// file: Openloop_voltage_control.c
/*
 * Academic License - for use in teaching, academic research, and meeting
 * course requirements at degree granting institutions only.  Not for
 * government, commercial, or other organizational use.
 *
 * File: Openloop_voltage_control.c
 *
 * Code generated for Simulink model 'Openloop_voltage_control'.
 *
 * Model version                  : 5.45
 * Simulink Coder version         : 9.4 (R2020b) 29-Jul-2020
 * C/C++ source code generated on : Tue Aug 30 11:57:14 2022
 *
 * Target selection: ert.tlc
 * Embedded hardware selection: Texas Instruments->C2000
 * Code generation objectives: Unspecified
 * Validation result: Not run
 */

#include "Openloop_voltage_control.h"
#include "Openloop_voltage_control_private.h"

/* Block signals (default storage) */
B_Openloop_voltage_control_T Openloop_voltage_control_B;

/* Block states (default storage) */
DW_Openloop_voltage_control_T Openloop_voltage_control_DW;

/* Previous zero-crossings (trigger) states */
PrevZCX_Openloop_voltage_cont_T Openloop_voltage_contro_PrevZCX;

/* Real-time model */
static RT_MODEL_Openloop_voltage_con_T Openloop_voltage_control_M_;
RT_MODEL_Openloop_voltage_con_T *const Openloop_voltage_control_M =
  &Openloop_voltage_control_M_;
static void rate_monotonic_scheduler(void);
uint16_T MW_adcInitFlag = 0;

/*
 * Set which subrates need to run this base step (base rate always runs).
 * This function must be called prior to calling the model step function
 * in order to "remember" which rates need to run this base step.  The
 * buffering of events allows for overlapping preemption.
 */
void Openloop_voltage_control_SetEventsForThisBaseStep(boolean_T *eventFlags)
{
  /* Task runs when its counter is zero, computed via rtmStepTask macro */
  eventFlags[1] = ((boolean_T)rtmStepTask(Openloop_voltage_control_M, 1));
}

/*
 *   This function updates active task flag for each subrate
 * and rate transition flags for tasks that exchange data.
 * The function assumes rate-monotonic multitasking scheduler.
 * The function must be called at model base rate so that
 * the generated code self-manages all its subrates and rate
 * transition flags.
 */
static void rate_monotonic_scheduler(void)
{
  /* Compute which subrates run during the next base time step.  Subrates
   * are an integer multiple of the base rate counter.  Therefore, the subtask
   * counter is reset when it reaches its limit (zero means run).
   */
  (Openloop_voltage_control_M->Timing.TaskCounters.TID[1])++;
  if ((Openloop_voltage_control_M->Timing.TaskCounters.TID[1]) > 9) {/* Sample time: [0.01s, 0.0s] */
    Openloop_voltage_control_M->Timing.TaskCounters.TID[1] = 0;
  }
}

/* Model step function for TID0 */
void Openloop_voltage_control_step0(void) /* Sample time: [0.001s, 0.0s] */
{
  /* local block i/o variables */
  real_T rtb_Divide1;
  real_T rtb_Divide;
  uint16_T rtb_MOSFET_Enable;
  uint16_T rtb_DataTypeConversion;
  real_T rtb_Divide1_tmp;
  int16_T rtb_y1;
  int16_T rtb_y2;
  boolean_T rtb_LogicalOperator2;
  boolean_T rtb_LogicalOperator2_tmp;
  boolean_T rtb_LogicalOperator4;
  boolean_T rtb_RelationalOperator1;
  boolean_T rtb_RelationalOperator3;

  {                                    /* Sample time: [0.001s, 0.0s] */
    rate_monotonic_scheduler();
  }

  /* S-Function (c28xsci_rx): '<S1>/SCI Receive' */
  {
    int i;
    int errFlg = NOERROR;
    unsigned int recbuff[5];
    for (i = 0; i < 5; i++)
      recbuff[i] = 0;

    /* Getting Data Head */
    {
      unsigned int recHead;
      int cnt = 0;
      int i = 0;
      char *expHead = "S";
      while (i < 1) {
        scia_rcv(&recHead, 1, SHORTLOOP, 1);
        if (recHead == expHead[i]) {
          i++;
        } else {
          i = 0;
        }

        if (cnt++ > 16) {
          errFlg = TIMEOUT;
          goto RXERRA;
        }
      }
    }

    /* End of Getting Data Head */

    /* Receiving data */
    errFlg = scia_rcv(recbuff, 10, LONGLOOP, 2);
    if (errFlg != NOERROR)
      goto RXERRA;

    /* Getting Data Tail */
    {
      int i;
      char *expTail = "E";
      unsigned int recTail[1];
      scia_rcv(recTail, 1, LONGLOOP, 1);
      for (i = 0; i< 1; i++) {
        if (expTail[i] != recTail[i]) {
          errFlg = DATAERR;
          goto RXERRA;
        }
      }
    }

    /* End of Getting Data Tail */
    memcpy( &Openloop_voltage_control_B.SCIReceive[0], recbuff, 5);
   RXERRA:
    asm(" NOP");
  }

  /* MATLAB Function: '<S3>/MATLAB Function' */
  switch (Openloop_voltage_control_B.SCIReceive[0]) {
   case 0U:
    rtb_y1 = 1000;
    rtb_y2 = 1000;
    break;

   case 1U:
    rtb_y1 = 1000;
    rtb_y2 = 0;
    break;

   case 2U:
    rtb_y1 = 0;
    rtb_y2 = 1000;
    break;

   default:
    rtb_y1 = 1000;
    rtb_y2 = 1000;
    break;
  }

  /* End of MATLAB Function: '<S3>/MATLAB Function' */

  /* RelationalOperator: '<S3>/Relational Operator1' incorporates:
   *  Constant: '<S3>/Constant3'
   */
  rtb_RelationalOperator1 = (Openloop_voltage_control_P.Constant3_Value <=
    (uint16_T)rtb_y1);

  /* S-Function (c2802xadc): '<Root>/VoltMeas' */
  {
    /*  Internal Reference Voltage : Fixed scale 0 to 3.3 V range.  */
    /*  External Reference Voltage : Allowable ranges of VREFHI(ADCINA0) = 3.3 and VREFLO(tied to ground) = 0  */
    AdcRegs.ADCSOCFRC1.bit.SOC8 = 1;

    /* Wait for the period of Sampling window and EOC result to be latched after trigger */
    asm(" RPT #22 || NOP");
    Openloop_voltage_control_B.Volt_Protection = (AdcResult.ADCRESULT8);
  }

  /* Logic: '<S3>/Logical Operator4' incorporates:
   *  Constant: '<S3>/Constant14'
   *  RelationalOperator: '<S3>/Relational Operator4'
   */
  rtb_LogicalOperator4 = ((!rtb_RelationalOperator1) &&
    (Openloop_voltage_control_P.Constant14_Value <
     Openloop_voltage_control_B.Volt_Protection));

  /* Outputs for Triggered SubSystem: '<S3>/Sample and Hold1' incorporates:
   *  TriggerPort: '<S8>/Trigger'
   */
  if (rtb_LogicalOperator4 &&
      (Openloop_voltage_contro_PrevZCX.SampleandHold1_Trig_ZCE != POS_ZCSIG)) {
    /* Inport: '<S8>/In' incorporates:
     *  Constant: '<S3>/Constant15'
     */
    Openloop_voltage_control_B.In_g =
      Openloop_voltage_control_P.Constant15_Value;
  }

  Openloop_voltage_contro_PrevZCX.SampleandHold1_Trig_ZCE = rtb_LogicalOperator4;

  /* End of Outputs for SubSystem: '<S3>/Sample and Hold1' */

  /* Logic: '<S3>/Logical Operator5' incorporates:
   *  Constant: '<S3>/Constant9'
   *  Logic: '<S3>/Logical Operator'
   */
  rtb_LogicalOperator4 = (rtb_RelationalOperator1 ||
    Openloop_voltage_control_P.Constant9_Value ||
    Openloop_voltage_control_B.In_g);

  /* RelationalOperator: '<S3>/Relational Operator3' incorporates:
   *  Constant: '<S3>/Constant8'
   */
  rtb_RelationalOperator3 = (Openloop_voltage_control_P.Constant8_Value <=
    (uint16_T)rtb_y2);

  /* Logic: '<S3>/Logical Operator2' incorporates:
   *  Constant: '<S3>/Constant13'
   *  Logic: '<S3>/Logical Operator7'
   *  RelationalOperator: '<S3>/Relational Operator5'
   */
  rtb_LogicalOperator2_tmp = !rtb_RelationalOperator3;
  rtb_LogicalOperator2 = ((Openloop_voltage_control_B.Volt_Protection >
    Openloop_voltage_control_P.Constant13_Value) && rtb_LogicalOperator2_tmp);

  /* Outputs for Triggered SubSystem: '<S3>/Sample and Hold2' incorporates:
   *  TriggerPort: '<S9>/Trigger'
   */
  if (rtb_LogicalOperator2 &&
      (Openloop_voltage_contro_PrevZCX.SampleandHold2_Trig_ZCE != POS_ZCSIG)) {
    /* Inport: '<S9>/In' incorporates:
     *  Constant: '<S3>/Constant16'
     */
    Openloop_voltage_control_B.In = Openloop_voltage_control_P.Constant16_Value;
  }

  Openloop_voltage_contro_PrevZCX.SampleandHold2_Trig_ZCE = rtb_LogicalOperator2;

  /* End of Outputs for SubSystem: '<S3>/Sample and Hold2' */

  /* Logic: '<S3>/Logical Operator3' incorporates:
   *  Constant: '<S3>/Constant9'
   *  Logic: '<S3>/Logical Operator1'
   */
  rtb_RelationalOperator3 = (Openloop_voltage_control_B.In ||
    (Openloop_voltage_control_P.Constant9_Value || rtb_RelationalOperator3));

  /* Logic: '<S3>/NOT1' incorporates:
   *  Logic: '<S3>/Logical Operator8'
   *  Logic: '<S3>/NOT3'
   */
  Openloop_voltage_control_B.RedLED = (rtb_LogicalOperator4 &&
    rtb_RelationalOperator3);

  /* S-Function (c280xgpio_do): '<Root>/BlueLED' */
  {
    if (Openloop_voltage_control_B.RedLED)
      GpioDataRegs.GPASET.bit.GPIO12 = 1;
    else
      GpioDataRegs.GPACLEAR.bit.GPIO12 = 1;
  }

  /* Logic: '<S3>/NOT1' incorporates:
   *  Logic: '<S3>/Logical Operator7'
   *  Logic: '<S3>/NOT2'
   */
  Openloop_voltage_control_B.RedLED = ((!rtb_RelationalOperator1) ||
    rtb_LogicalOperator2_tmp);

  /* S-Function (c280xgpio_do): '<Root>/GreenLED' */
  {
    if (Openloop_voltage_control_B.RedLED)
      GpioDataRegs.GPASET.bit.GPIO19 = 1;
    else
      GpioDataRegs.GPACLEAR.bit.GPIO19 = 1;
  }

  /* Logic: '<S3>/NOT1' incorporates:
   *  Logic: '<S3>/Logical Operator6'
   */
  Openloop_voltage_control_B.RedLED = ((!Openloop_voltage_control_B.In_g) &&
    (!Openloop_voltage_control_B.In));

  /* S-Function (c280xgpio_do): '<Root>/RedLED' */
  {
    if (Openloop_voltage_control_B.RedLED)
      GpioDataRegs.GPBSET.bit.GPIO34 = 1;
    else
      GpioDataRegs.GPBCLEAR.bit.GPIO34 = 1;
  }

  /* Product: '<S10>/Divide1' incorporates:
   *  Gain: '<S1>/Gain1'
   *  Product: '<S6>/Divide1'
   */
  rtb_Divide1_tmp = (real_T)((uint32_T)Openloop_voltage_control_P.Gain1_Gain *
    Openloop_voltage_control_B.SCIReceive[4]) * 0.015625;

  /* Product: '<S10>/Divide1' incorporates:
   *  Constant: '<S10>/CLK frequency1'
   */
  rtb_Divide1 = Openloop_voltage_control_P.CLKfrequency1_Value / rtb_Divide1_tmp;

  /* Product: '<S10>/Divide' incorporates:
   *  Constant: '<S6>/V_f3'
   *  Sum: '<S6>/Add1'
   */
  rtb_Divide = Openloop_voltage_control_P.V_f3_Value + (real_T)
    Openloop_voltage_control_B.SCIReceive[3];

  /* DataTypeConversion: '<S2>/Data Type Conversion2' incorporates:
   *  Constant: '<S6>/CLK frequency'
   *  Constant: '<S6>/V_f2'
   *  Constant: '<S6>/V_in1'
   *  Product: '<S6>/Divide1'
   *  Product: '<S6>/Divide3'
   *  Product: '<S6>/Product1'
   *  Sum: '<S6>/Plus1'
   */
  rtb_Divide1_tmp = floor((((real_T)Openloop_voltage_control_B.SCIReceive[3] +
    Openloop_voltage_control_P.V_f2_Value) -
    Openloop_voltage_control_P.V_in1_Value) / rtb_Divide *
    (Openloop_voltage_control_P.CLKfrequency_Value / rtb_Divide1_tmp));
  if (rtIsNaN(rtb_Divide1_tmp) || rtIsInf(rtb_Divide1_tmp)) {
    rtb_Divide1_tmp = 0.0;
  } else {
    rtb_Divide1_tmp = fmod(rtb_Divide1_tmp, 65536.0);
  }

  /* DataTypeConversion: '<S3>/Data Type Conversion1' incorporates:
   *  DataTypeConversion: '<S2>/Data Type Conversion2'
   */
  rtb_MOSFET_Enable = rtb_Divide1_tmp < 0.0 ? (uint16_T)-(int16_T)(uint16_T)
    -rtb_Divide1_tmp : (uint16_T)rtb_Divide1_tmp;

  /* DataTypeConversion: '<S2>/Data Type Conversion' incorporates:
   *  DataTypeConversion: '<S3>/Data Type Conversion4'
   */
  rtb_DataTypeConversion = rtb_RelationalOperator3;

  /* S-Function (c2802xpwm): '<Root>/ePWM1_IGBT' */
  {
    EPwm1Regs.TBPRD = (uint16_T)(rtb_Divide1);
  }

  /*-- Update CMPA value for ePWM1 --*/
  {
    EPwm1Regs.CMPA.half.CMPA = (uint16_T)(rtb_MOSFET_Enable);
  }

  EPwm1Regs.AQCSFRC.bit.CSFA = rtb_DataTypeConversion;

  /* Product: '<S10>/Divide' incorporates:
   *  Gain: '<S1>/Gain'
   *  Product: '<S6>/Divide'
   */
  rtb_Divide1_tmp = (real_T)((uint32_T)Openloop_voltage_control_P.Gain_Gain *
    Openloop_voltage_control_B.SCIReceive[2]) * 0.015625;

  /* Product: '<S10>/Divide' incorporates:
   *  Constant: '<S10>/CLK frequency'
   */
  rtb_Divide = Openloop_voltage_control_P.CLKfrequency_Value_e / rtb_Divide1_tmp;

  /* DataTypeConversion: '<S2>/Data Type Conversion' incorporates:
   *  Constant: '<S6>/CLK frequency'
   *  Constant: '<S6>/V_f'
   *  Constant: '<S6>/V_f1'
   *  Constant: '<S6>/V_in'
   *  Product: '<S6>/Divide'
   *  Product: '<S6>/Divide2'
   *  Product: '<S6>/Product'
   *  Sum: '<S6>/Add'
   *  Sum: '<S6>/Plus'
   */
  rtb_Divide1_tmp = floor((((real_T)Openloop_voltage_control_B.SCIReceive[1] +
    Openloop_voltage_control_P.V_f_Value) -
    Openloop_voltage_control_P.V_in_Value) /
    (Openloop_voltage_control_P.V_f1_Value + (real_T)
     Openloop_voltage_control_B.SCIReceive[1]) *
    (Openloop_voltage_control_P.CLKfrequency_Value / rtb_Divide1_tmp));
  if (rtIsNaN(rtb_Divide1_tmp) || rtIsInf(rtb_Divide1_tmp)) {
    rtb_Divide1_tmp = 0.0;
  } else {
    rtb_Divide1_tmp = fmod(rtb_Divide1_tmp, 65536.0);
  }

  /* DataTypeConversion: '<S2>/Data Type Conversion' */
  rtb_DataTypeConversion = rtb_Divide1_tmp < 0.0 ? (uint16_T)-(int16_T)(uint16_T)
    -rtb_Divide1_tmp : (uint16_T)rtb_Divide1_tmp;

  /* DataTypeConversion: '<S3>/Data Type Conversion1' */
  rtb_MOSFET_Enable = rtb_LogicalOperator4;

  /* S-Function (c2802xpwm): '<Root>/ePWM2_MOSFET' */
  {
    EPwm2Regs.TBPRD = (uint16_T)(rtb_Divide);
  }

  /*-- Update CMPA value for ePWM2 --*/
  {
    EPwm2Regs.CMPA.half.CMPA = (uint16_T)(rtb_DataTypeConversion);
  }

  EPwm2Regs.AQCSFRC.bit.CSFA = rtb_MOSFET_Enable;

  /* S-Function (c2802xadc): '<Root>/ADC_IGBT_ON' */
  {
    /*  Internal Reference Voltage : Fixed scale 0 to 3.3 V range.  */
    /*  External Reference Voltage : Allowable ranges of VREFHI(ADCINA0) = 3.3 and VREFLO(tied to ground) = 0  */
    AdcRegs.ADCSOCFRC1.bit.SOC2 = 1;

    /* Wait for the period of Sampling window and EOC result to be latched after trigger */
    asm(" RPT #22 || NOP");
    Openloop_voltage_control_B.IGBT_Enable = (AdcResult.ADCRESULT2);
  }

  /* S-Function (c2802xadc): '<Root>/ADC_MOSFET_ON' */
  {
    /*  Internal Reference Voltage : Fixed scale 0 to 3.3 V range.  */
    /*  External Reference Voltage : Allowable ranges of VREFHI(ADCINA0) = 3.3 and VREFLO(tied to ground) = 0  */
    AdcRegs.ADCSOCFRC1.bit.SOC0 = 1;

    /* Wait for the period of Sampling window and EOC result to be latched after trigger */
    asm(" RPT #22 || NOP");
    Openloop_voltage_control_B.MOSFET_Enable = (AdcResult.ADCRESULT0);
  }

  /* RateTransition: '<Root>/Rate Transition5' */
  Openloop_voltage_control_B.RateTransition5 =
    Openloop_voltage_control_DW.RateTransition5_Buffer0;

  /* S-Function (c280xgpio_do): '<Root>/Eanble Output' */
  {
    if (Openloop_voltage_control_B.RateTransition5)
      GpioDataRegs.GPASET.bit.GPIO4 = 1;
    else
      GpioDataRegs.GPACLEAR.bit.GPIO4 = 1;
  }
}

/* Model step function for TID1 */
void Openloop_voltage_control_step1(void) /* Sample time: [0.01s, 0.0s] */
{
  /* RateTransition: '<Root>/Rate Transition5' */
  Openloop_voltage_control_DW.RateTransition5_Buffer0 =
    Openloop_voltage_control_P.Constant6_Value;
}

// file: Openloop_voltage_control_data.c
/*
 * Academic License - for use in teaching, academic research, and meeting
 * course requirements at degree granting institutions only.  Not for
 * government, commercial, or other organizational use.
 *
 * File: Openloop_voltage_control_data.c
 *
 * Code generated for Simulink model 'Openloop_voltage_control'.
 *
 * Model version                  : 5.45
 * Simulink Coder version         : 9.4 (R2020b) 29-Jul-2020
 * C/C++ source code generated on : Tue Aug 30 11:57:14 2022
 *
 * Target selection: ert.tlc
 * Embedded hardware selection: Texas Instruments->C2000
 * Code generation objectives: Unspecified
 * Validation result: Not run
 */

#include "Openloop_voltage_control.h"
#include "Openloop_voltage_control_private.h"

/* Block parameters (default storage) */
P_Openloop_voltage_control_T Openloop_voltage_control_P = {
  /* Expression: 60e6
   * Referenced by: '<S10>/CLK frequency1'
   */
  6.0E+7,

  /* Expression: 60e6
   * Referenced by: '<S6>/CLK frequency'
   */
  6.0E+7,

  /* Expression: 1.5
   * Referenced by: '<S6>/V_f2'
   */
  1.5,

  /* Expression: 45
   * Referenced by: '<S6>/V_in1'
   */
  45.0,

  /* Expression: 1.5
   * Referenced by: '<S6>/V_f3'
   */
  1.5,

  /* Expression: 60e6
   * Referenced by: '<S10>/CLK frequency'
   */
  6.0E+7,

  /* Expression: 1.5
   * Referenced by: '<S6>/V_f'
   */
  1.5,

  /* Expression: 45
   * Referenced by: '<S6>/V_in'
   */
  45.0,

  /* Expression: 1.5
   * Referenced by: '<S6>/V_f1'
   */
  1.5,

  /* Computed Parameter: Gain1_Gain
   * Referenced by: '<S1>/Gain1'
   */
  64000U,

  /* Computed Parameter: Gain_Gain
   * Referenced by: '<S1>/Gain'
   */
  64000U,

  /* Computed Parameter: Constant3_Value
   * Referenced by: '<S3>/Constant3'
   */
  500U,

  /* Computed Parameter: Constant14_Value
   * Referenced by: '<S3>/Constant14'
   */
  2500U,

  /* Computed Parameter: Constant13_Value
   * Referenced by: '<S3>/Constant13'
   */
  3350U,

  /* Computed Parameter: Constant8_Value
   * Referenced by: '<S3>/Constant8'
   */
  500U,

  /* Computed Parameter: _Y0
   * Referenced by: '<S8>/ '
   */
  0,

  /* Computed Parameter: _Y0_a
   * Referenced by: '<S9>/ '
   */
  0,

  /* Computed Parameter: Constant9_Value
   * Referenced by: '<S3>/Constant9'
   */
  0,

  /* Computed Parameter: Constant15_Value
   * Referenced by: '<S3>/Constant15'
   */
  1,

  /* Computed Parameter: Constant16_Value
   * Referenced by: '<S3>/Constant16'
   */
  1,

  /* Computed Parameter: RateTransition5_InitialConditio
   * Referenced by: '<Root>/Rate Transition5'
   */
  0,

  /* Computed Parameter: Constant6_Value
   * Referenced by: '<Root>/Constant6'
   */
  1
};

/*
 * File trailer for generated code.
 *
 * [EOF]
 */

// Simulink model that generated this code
simulink model "Openloop_voltage_control"  (R2020b)
settings: Solver=FixedStepDiscrete  StartTime=0.0  StopTime=Inf  RelTol=1e-3  EnableMultiTasking=on
undefined symbols (not defined in the file): C2000, Clear, D_IGBT_CCM, D_MOSFET_CCM, Disable, ePWM2, ePWMxA, GPTRIP1SEL, GPTRIP2SEL, Immediate, Positive, Set, Timer_period_IGBT, Timer_period_MOSFET, TZ1, TZ2, Up
libraries: c2802xlib x9, dspsigops x2, c280xlib x1

== system Openloop_voltage_control ==
  note: Enable PWM
  ADC_IGBT_ON : c2802xlib/ADC  blkParamProc=C2000  ADCModule=1  samplingMode=Single sample mode  ADCResolution=12-bit (Single-ended input)  useSOC1=SOC2  useSOC2=SOC0_SOC1  SOCAcquisitionWindow=7  SOCTriggerSource=Software  SOCInterruptTrigger=No ADCINT  Ts=0.001  dType=uint16  postInterrupt=off  interruptSel=ADCINT1  ADCINTContinuous=off  endma=off  chdma=1  conv1=ADCINA3  conv2=ADCINA7 and ADCINB7  conv1_Type4=ADCIN0  conv2_Type4=ADCIN0 and ADCIN1
  ADC_MOSFET_ON : c2802xlib/ADC  blkParamProc=C2000  ADCModule=1  samplingMode=Single sample mode  ADCResolution=12-bit (Single-ended input)  useSOC1=SOC0  useSOC2=SOC0_SOC1  SOCAcquisitionWindow=7  SOCTriggerSource=Software  SOCInterruptTrigger=No ADCINT  Ts=0.001  dType=uint16  postInterrupt=off  interruptSel=ADCINT1  ADCINTContinuous=off  endma=off  chdma=1  conv1=ADCINA7  conv2=ADCINA7 and ADCINB7  conv1_Type4=ADCIN0  conv2_Type4=ADCIN0 and ADCIN1
  BlueLED : c2802xlib/Digital Output  GPIO_Number=GPIO8~GPIO15  GPIO_Bit0=off  GPIO_BIT0_Toggle=off  GPIO_Bit1=off  GPIO_BIT1_Toggle=off  GPIO_Bit2=off  GPIO_BIT2_Toggle=off  GPIO_Bit3=off  GPIO_BIT3_Toggle=off  GPIO_Bit4=on  GPIO_BIT4_Toggle=off  GPIO_Bit5=off  GPIO_BIT5_Toggle=off  GPIO_Bit6=off  GPIO_BIT6_Toggle=off  GPIO_Bit7=off  GPIO_BIT7_Toggle=off
  Constant6 : Constant  OutDataTypeStr=boolean  SampleTime=0.01
  Dashboard receiver block : Subsystem
  Demux : Demux  Outputs=3
  Duty Cycles : Subsystem
  Eanble Output : c2802xlib/Digital Output  GPIO_Number=GPIO0~GPIO7  GPIO_Bit0=off  GPIO_BIT0_Toggle=off  GPIO_Bit1=off  GPIO_BIT1_Toggle=off  GPIO_Bit2=off  GPIO_BIT2_Toggle=off  GPIO_Bit3=off  GPIO_BIT3_Toggle=off  GPIO_Bit4=on  GPIO_BIT4_Toggle=off  GPIO_Bit5=off  GPIO_BIT5_Toggle=off  GPIO_Bit6=off  GPIO_BIT6_Toggle=off  GPIO_Bit7=off  GPIO_BIT7_Toggle=off
  GreenLED : c2802xlib/Digital Output  GPIO_Number=GPIO16~GPIO23  GPIO_Bit0=off  GPIO_BIT0_Toggle=off  GPIO_Bit1=off  GPIO_BIT1_Toggle=off  GPIO_Bit2=off  GPIO_BIT2_Toggle=off  GPIO_Bit3=on  GPIO_BIT3_Toggle=off  GPIO_Bit4=off  GPIO_BIT4_Toggle=off  GPIO_Bit5=off  GPIO_BIT5_Toggle=off  GPIO_Bit6=off  GPIO_BIT6_Toggle=off  GPIO_Bit7=off  GPIO_BIT7_Toggle=off
  Logic circuit : Subsystem
  Rate Transition10 : RateTransition  Deterministic=off
  Rate Transition3 : RateTransition
  Rate Transition5 : RateTransition  Deterministic=off
  Rate Transition7 : RateTransition
  Rate Transition8 : RateTransition  Deterministic=off  InitialCondition=1
  Rate Transition9 : RateTransition  Deterministic=off
  RedLED : c2802xlib/Digital Output  GPIO_Number=GPIO32~GPIO34  GPIO_Bit0=off  GPIO_BIT0_Toggle=off  GPIO_Bit1=off  GPIO_BIT1_Toggle=off  GPIO_Bit2=on  GPIO_BIT2_Toggle=off  GPIO_Bit3=off  GPIO_BIT3_Toggle=off  GPIO_Bit4=off  GPIO_BIT4_Toggle=off  GPIO_Bit5=off  GPIO_BIT5_Toggle=off  GPIO_Bit6=off  GPIO_BIT6_Toggle=off  GPIO_Bit7=off  GPIO_BIT7_Toggle=off
  Timer : Subsystem
  VoltMeas : c2802xlib/ADC  blkParamProc=C2000  ADCModule=1  samplingMode=Single sample mode  ADCResolution=12-bit (Single-ended input)  useSOC1=SOC8  useSOC2=SOC0_SOC1  SOCAcquisitionWindow=7  SOCTriggerSource=Software  SOCInterruptTrigger=No ADCINT  Ts=0.001  dType=uint16  postInterrupt=off  interruptSel=ADCINT1  ADCINTContinuous=off  endma=off  chdma=1  conv1=ADCINB1  conv2=ADCINA7 and ADCINB7  conv1_Type4=ADCIN0  conv2_Type4=ADCIN0 and ADCIN1
  ePWM1_IGBT : c2802xlib/ePWM  PwmType=C2000  useModule=ePWM1  ePWMxLINKTBPRD=Not Linked  periodUnits=Clock cycles  timerSource=Input port  timerPeriod_clk=Timer_period_IGBT*2  timerPeriod_sec=0.0001  tbshadow=Counter equals to zero  countingMode=Up  phaseActiveEnable=Disable  phaseDirection=Count down after sync  phaseActive=0  synchronizationEnable=off  dcaevt1Sync=off  dcbevt1Sync=off  synchronizationOption=Disable  perSynchronizationOption=Counter equals to period (CTR=PRD)  clockPrescale=1  HSclockPrescale=1  enswap=off  ePWMxAStatus=on  ePWMxAactionLogic1=Set  ePWMxAactionLogic2=Set  ePWMxAactionLogic3=Clear  ePWMxAactionLogic4=Set  ePWMxAactionLogic5=Do nothing  ePWMxAactionLogic6=Do nothing  ePWMxACSFenable=on  ePWMxACSFvalue=Forcing disable  ePWMxASFreload=Immediate  ePWMxBStatus=off  ePWMxBactionLogic1=Set  ePWMxBactionLogic2=Clear  ePWMxBactionLogic3=Do nothing  ePWMxBactionLogic4=Do nothing  ePWMxBactionLogic5=Clear  ePWMxBactionLogic6=Set  ePWMxBCSFenable=off  ePWMxBCSFvalue=Forcing disable  ePWMxBSFreload=Immediate  ePWNxBOutWay=off  ePWMxLINKCMPA=Not Linked  CMPAUnits=Clock cycles  CMPASource=Input port  CMPAValue_per=50  CMPAValue_clk=2000  enCMPAshadow=Counter equals to zero (CTR=Zero)  ePWMxLINKCMPB=Not Linked  CMPBUnits=Clock cycles  CMPBSource=Specify via dialog  CMPBValue_per=50  CMPBValue_clk=32000  enCMPBshadow=Counter equals to zero (CTR=Zero)  ePWMxLINKCMPC=Not Linked  CMPCUnits=Clock cycles  CMPCSource=Specify via dialog  CMPCValue_per=50  CMPCValue_clk=32000  enCMPCshadow=Counter equals to zero (CTR=Zero)  ePWMxLINKCMPD=Not Linked  CMPDUnits=Clock cycles  CMPDSource=Specify via dialog  CMPDValue_per=50  CMPDValue_clk=32000  enCMPDshadow=Counter equals to zero (CTR=Zero)  enableDBePWMxA=off  enableDBePWMxB=off  enhalfcycle=off  DBpolarity=Active high (AH)  DBedgeDelay=Positive  DBSource_ePWMxA=ePWMxA  DBSource_ePWMxB=ePWMxA  DBPeriodUnits=Clock cycles  DBperiodSource=Specify via dialog  REDperiod=0  FEDperiod=0  REDperiod_sec=0  FEDperiod_sec=0  LoadModeDBRED=Immediate without using shadow  LoadModeDBFED=Immediate without using shadow  adcstartModuleA=off  adcrequestEventA=First event  adcstartEventA=Digital Compare Module A Event 1 start of conversion (DCAEVT1.soc)  adcstartEventA_type2=Digital Compare Module A Event 1 start of conversion (DCAEVT1.soc)  adcstartModuleB=off  adcrequestEventB=First event  adcstartEventB=Counter equals to zero (CTR=Zero)  adcstartEventB_type2=Counter equals to zero (CTR=Zero)  intEn=off  intPrd=First event  intSel=Counter equals to zero (CTR=Zero)  intSel_type2=Counter equals to zero (CTR=Zero)  hrpe=off  enHRPWM=off  HRPWM_LoadMode=Counter equals to period (CTR=PRD)  HRPWM_CTLMode=Duty or Period control mode  HRPWM_EDGMode=Both edge  hrpeb=off  enHRPWMB=off  HRPWM_LoadModeB=Counter equals to zero (CTR=ZERO)  HRPWM_CTLModeB=Duty or Period control mode  HRPWM_EDGModeB=Both edge  enHRDBRED=off  enHRDBFED=off  enSFO=on  enautoconv=on  chopperEnable=off  chopperFrequency=1  chopperFirstwidth=1  chopperDuty=12.5%  tripZonesource=Specify via dialog  tzselOSHT1=off  tzselOSHT2=off  tzselOSHT3=off  tzselOSHDCAEV1=off  tzselOSHDCBEV1=off  tzselCBC1=off  tzselCBC2=off  tzselCBC3=off  tzselCBCDCAEV2=off  tzselCBCDCBEV2=off  tzselOSHT4=off  tzselOSHT5=off  tzselOSHT6=off  tzselCBC4=off  tzselCBC5=off  tzselCBC6=off  enTzOstIntr=off  enTzCbcIntr=off  enTzDCAEVT1Intr=off  enTzDCAEVT2Intr=off  enTzDCBEVT1Intr=off  enTzDCBEVT2Intr=off  ePWMxAforced=No action  ePWMxBforced=No action  DCAEVT1forced=No action  DCBEVT1forced=No action  DCAEVT2forced=No action  DCBEVT2forced=No action  dcah=Trip Zone 1 input (TZ1)  dcal=Trip Zone 2 input (TZ2)  dcbh=Trip Zone 1 input (TZ1)  dcbl=Trip Zone 2 input (TZ2)  dcah_type2=GPTRIP1SEL/(TZ1)  dcal_type2=GPTRIP2SEL/(TZ2)  dcbh_type2=GPTRIP1SEL/(TZ1)  dcbl_type2=GPTRIP2SEL/(TZ2)  gendcaevt1=Event disabled  gendcaevt2=Event disabled  gendcbevt1=Event disabled  gendcbevt2=Event disabled  dcaevt1src=DCAEVT1 with sync  dcaevt2src=DCAEVT2 with sync  dcbevt1src=DCBEVT1 with sync  dcbevt2src=DCBEVT2 with sync  pulsesel=Counter equals to zero (CTR=Zero)  blankinv=off  blankoffset=0  blankwidth=0  evsrcsel=Filtered version of DCAEVT1 (DCAEVT1FILT)  encape=off
  ePWM2_MOSFET : c2802xlib/ePWM  PwmType=C2000  useModule=ePWM2  ePWMxLINKTBPRD=Not Linked  periodUnits=Clock cycles  timerSource=Input port  timerPeriod_clk=timerPeriod_clk  timerPeriod_sec=timerPeriod_sec  tbshadow=Counter equals to zero  countingMode=Up  phaseActiveEnable=Disable  phaseDirection=Count down after sync  phaseActive=phaseActive  synchronizationEnable=off  dcaevt1Sync=off  dcbevt1Sync=off  synchronizationOption=Disable  perSynchronizationOption=Counter equals to period (CTR=PRD)  clockPrescale=1  HSclockPrescale=1  enswap=off  ePWMxAStatus=on  ePWMxAactionLogic1=Set  ePWMxAactionLogic2=Set  ePWMxAactionLogic3=Clear  ePWMxAactionLogic4=Set  ePWMxAactionLogic5=Do nothing  ePWMxAactionLogic6=Do nothing  ePWMxACSFenable=on  ePWMxACSFvalue=Forcing disable  ePWMxASFreload=Immediate  ePWMxBStatus=off  ePWMxBactionLogic1=Set  ePWMxBactionLogic2=Clear  ePWMxBactionLogic3=Do nothing  ePWMxBactionLogic4=Do nothing  ePWMxBactionLogic5=Clear  ePWMxBactionLogic6=Set  ePWMxBCSFenable=off  ePWMxBCSFvalue=Forcing disable  ePWMxBSFreload=Immediate  ePWNxBOutWay=off  ePWMxLINKCMPA=Not Linked  CMPAUnits=Clock cycles  CMPASource=Input port  CMPAValue_per=CMPAValue_per  CMPAValue_clk=CMPAValue_clk  enCMPAshadow=Counter equals to zero (CTR=Zero)  ePWMxLINKCMPB=Not Linked  CMPBUnits=Clock cycles  CMPBSource=Specify via dialog  CMPBValue_per=CMPBValue_per  CMPBValue_clk=CMPBValue_clk  enCMPBshadow=Counter equals to zero (CTR=Zero)  ePWMxLINKCMPC=Not Linked  CMPCUnits=Clock cycles  CMPCSource=Specify via dialog  CMPCValue_per=CMPCValue_per  CMPCValue_clk=CMPCValue_clk  enCMPCshadow=Counter equals to zero (CTR=Zero)  ePWMxLINKCMPD=Not Linked  CMPDUnits=Clock cycles  CMPDSource=Specify via dialog  CMPDValue_per=CMPDValue_per  CMPDValue_clk=CMPDValue_clk  enCMPDshadow=Counter equals to zero (CTR=Zero)  enableDBePWMxA=off  enableDBePWMxB=off  enhalfcycle=off  DBpolarity=Active high (AH)  DBedgeDelay=Positive  DBSource_ePWMxA=ePWMxA  DBSource_ePWMxB=ePWMxA  DBPeriodUnits=Clock cycles  DBperiodSource=Specify via dialog  REDperiod=REDperiod  FEDperiod=FEDperiod  REDperiod_sec=REDperiod_sec  FEDperiod_sec=FEDperiod_sec  LoadModeDBRED=Immediate without using shadow  LoadModeDBFED=Immediate without using shadow  adcstartModuleA=off  adcrequestEventA=First event  adcstartEventA=Digital Compare Module A Event 1 start of conversion (DCAEVT1.soc)  adcstartEventA_type2=Digital Compare Module A Event 1 start of conversion (DCAEVT1.soc)  adcstartModuleB=off  adcrequestEventB=First event  adcstartEventB=Counter equals to zero (CTR=Zero)  adcstartEventB_type2=Counter equals to zero (CTR=Zero)  intEn=off  intPrd=First event  intSel=Counter equals to zero (CTR=Zero)  intSel_type2=Counter equals to zero (CTR=Zero)  hrpe=off  enHRPWM=off  HRPWM_LoadMode=Counter equals to period (CTR=PRD)  HRPWM_CTLMode=Duty or Period control mode  HRPWM_EDGMode=Both edge  hrpeb=off  enHRPWMB=off  HRPWM_LoadModeB=Counter equals to zero (CTR=ZERO)  HRPWM_CTLModeB=Duty or Period control mode  HRPWM_EDGModeB=Both edge  enHRDBRED=off  enHRDBFED=off  enSFO=on  enautoconv=on  chopperEnable=off  chopperFrequency=1  chopperFirstwidth=1  chopperDuty=12.5%  tripZonesource=Specify via dialog  tzselOSHT1=off  tzselOSHT2=off  tzselOSHT3=off  tzselOSHDCAEV1=off  tzselOSHDCBEV1=off  tzselCBC1=off  tzselCBC2=off  tzselCBC3=off  tzselCBCDCAEV2=off  tzselCBCDCBEV2=off  tzselOSHT4=off  tzselOSHT5=off  tzselOSHT6=off  tzselCBC4=off  tzselCBC5=off  tzselCBC6=off  enTzOstIntr=off  enTzCbcIntr=off  enTzDCAEVT1Intr=off  enTzDCAEVT2Intr=off  enTzDCBEVT1Intr=off  enTzDCBEVT2Intr=off  ePWMxAforced=No action  ePWMxBforced=No action  DCAEVT1forced=No action  DCBEVT1forced=No action  DCAEVT2forced=No action  DCBEVT2forced=No action  dcah=Trip Zone 1 input (TZ1)  dcal=Trip Zone 2 input (TZ2)  dcbh=Trip Zone 1 input (TZ1)  dcbl=Trip Zone 2 input (TZ2)  dcah_type2=GPTRIP1SEL/(TZ1)  dcal_type2=GPTRIP2SEL/(TZ2)  dcbh_type2=GPTRIP1SEL/(TZ1)  dcbl_type2=GPTRIP2SEL/(TZ2)  gendcaevt1=Event disabled  gendcaevt2=Event disabled  gendcbevt1=Event disabled  gendcbevt2=Event disabled  dcaevt1src=DCAEVT1 with sync  dcaevt2src=DCAEVT2 with sync  dcbevt1src=DCBEVT1 with sync  dcbevt2src=DCBEVT2 with sync  pulsesel=Counter equals to zero (CTR=Zero)  blankinv=off  blankoffset=blankoffset  blankwidth=blankwidth  evsrcsel=Filtered version of DCAEVT1 (DCAEVT1FILT)  encape=off  mask(C2802x/03x/05x/06x/M3x/37x/07x/004x/38x ePWM){PwmType=C2000, useModule=ePWM2, ePWMxLINKTBPRD=Not Linked, periodUnits=Clock cycles, timerSource=Input port, timerPeriod_clk=Timer_period_MOSFET*2, timerPeriod_sec=0.0001, tbshadow=Counter equals to zero, countingMode=Up, phaseActiveEnable=Disable, phaseDirection=Count down after sync, phaseActive=0, synchronizationEnable=off, dcaevt1Sync=off, dcbevt1Sync=off, synchronizationOption=Disable, perSynchronizationOption=Counter equals to period (CTR=PRD), clockPrescale=1, HSclockPrescale=1, enswap=off, ePWMxAStatus=on, ePWMxAactionLogic1=Set, ePWMxAactionLogic2=Set, ePWMxAactionLogic3=Clear, ePWMxAactionLogic4=Set, ePWMxAactionLogic5=Do nothing, ePWMxAactionLogic6=Do nothing, ePWMxACSFenable=on, ePWMxACSFvalue=Forcing disable, ePWMxASFreload=Immediate, ePWMxBStatus=off, ePWMxBactionLogic1=Set, ePWMxBactionLogic2=Clear, ePWMxBactionLogic3=Do nothing, ePWMxBactionLogic4=Do nothing, ePWMxBactionLogic5=Clear, ePWMxBactionLogic6=Set, ePWMxBCSFenable=off, ePWMxBCSFvalue=Forcing disable, ePWMxBSFreload=Immediate, ePWNxBOutWay=off, ePWMxLINKCMPA=Not Linked, CMPAUnits=Clock cycles, CMPASource=Input port, CMPAValue_per=50, CMPAValue_clk=525, enCMPAshadow=Counter equals to zero (CTR=Zero), ePWMxLINKCMPB=Not Linked, CMPBUnits=Clock cycles, CMPBSource=Specify via dialog, CMPBValue_per=50, CMPBValue_clk=32000, enCMPBshadow=Counter equals to zero (CTR=Zero), ePWMxLINKCMPC=Not Linked, CMPCUnits=Clock cycles, CMPCSource=Specify via dialog, CMPCValue_per=50, CMPCValue_clk=32000, enCMPCshadow=Counter equals to zero (CTR=Zero), ePWMxLINKCMPD=Not Linked, CMPDUnits=Clock cycles, CMPDSource=Specify via dialog, CMPDValue_per=50, CMPDValue_clk=32000, enCMPDshadow=Counter equals to zero (CTR=Zero), enableDBePWMxA=off, enableDBePWMxB=off, enhalfcycle=off, DBpolarity=Active high (AH), DBedgeDelay=Positive, DBSource_ePWMxA=ePWMxA, DBSource_ePWMxB=ePWMxA, DBPeriodUnits=Clock cycles, DBperiodSource=Specify via dialog, REDperiod=0, FEDperiod=0, REDperiod_sec=0, FEDperiod_sec=0, LoadModeDBRED=Immediate without using shadow, LoadModeDBFED=Immediate without using shadow, adcstartModuleA=off, adcrequestEventA=First event, adcstartEventA=Digital Compare Module A Event 1 start of conversion (DCAEVT1.soc), adcstartEventA_type2=Digital Compare Module A Event 1 start of conversion (DCAEVT1.soc), adcstartModuleB=off, adcrequestEventB=First event, adcstartEventB=Counter equals to zero (CTR=Zero), adcstartEventB_type2=Counter equals to zero (CTR=Zero), intEn=off, intPrd=First event, intSel=Counter equals to zero (CTR=Zero), intSel_type2=Counter equals to zero (CTR=Zero), hrpe=off, enHRPWM=off, HRPWM_LoadMode=Counter equals to period (CTR=PRD), HRPWM_CTLMode=Duty or Period control mode, HRPWM_EDGMode=Both edge, hrpeb=off, enHRPWMB=off, HRPWM_LoadModeB=Counter equals to zero (CTR=ZERO), HRPWM_CTLModeB=Duty or Period control mode, HRPWM_EDGModeB=Both edge, enHRDBRED=off, enHRDBFED=off, enSFO=on, enautoconv=on, chopperEnable=off, chopperFrequency=1, chopperFirstwidth=1, chopperDuty=12.5%, tripZonesource=Specify via dialog, tzselOSHT1=off, tzselOSHT2=off, tzselOSHT3=off, tzselOSHDCAEV1=off, tzselOSHDCBEV1=off, tzselCBC1=off, tzselCBC2=off, tzselCBC3=off, tzselCBCDCAEV2=off, tzselCBCDCBEV2=off, tzselOSHT4=off, tzselOSHT5=off, tzselOSHT6=off, tzselCBC4=off, tzselCBC5=off, tzselCBC6=off, enTzOstIntr=off, enTzCbcIntr=off, enTzDCAEVT1Intr=off, enTzDCAEVT2Intr=off, enTzDCBEVT1Intr=off, enTzDCBEVT2Intr=off, ePWMxAforced=No action, ePWMxBforced=No action, DCAEVT1forced=No action, DCBEVT1forced=No action, DCAEVT2forced=No action, DCBEVT2forced=No action, dcah=Trip Zone 1 input (TZ1), dcal=Trip Zone 2 input (TZ2), dcbh=Trip Zone 1 input (TZ1), dcbl=Trip Zone 2 input (TZ2), dcah_type2=GPTRIP1SEL/(TZ1), dcal_type2=GPTRIP2SEL/(TZ2), dcbh_type2=GPTRIP1SEL/(TZ1), dcbl_type2=GPTRIP2SEL/(TZ2), gendcaevt1=Event disabled, gendcaevt2=Event disabled, gendcbevt1=Event disabled, gendcbevt2=Event disabled, dcaevt1src=DCAEVT1 with sync, dcaevt2src=DCAEVT2 with sync, dcbevt1src=DCBEVT1 with sync, dcbevt2src=DCBEVT2 with sync, pulsesel=Counter equals to zero (CTR=Zero), blankinv=off, blankoffset=0, blankwidth=0, evsrcsel=Filtered version of DCAEVT1 (DCAEVT1FILT), encape=off}
      mask prompts: PwmType "BlockParameterProcessor"; useModule "Module:"; ePWMxLINKTBPRD "ePWMLink TBPRD"; periodUnits "Timer period units:"; timerSource "Specify timer period via:"; timerPeriod_clk "Timer period:"; timerPeriod_sec "Timer period:"; tbshadow "Reload for time base period register (PRDLD):"; countingMode "Counting mode:"; phaseActiveEnable "Synchronization action:"; phaseDirection "Counting direction after phase synchronization:"; phaseActive "Phase offset value (TBPHS):"; synchronizationEnable "Specify software synchronization via input port (SWFSYNC)"; dcaevt1Sync "Enable digital compare A event1 synchronization (DCAEVT1)"; dcbevt1Sync "Enable digital compare B event1 synchronization (DCBEVT1)"; synchronizationOption "Synchronization output (SYNCO):"; perSynchronizationOption "Peripheral synchronization event (PWMSYNCSEL):"; clockPrescale "Time base clock (TBCLK) prescaler divider:"; HSclockPrescale "High speed time base clock (HSPCLKDIV) prescaler divider:"; enswap "Enable swap module A and B"; ePWMxAStatus "Enable ePWM2A"; ePWMxAactionLogic1 "Action when counter=ZERO:"; ePWMxAactionLogic2 "Action when counter=period (PRD):"; ePWMxAactionLogic3 "Action when counter=CMPA on up-count (CAU):"; ePWMxAactionLogic4 "Action when counter=CMPA on down-count (CAD):"; ePWMxAactionLogic5 "Action when counter=CMPB on up-count (CBU):"; ePWMxAactionLogic6 "Action when counter=CMPB on down-count (CBD):"; ePWMxACSFenable "Add continuous software force input port"; ePWMxACSFvalue "Continuous software force logic:"; ePWMxASFreload "Reload condition for software force:"; ePWMxBStatus "Enable ePWM2B"; ePWMxBactionLogic1 "Action when counter=ZERO:"; ePWMxBactionLogic2 "Action when counter=period (PRD):"; ePWMxBactionLogic3 "Action when counter=CMPA on up-count (CAU):"; ePWMxBactionLogic4 "Action when counter=CMPA on down-count (CAD):"; ePWMxBactionLogic5 "Action when counter=CMPB on up-count (CBU):"; ePWMxBactionLogic6 "Action when counter=CMPB on down-count (CBD):"; ePWMxBCSFenable "Add continuous software force input port"; ePWMxBCSFvalue "Continuous software force logic:"; ePWMxBSFreload "Reload condition for software force:"; ePWNxBOutWay "Inverted version of ePWMxA"; ePWMxLINKCMPA "ePWMLink CMPA"; CMPAUnits "CMPA units:"; CMPASource "Specify CMPA via:"; CMPAValue_per "CMPA initial value:"; CMPAValue_clk "CMPA initial value:"; enCMPAshadow "Reload for compare A Register (SHDWAMODE):"; ePWMxLINKCMPB "ePWMLink CMPB"; CMPBUnits "CMPB units:"; CMPBSource "Specify CMPB via:"; CMPBValue_per "CMPB value:"; CMPBValue_clk "CMPB value:"; enCMPBshadow "Reload for compare B Register (SHDWBMODE):"; ePWMxLINKCMPC "ePWMLink CMPC"; CMPCUnits "CMPC units:"; CMPCSource "Specify CMPC via:"; CMPCValue_per "CMPC value:"; CMPCValue_clk "CMPC value:"; enCMPCshadow "Reload for compare C Register (SHDWCMODE):"; ePWMxLINKCMPD "ePWMLink CMPD"; CMPDUnits "CMPD units:"; CMPDSource "Specify CMPD via:"; CMPDValue_per "CMPD value:"; CMPDValue_clk "CMPD value:"; enCMPDshadow "Reload for compare D Register (SHDWDMODE):"; enableDBePWMxA "Use deadband for ePWM2A"; enableDBePWMxB "Use deadband for ePWM2B"; enhalfcycle "Enable half-cycle clocking"; DBpolarity "Deadband polarity:"; DBedgeDelay "Deadband polarity:"; DBSource_ePWMxA "Signal source for raising edge (RED):"; DBSource_ePWMxB "Signal source for falling edge (FED):"; DBPeriodUnits "Deadband period units:"; DBperiodSource "Deadband period source:"; REDperiod "Deadband Rising edge (RED) period (0~1023):"; FEDperiod "Deadband Falling edge (FED) period (0~1023):"; REDperiod_sec "Deadband Rising edge (RED) period:"; FEDperiod_sec "Deadband Falling edge (FED) period:"; LoadModeDBRED "Reload for DBRED register (SHDWDBRED):"; LoadModeDBFED "Reload for DBFED register (SHDWDBFED):"; adcstartModuleA "Enable ADC start of conversion for module A"; adcrequestEventA "Number of event for start of conversion A (SOCA) to be generated:"; adcstartEventA "Start of conversion for module A event selection:"; adcstartEventA_type2 "Start of conversion for module A event selection:"; adcstartModuleB "Enable ADC start of conversion for module B"; adcrequestEventB "Number of event for start of conversion B (SOCB) to be generated:"; adcstartEventB "Start of conversion for module B event selection:"; adcstartEventB_type2 "Start of conversion for module B event selection:"; intEn "Enable ePWM interrupt"; intPrd "Number of event for interrupt to be generated:"; intSel "Interrupt counter match event condition:"; intSel_type2 "Interrupt counter match event condition:"; hrpe "Enable High Resolution Period on ePWMxA(HRPWM-period)"; enHRPWM "Enable HRPWM Duty on ePWMxA(HRPWM-duty)"; HRPWM_LoadMode "High resolution PWM (HRPWM) Load mode on ePWMxA:"; HRPWM_CTLMode "High resolution PWM (HRPWM) control mode on ePWMxA:"; HRPWM_EDGMode "High resolution PWM (HRPWM) edge control mode on ePWMxA:"; hrpeb "Enable High Resolution Period on ePWMxB (HRPWM-period)"; enHRPWMB "Enable HRPWM Duty on ePWMxB (HRPWM-duty)"; HRPWM_LoadModeB "High resolution PWM (HRPWM) Load mode on ePWMxB:"; HRPWM_CTLModeB "High resolution PWM (HRPWM) control mode on ePWMxB:"; HRPWM_EDGModeB "High resolution PWM (HRPWM) edge control mode on ePWMxB:"; enHRDBRED "Enable high resolution deadband rising edge (RED)"; enHRDBFED "Enable high resolution deadband falling edge (FED)"; enSFO "Use scale factor optimizer (SFO) software"; enautoconv "Enable auto convert"; chopperEnable "Chopper module enable"; chopperFrequency "Chopper frequency divider:"; chopperFirstwidth "Chopper clock cycles width of first pulse:"; chopperDuty "Chopper pulse duty cycle:"; tripZonesource "Trip zone source:"; tzselOSHT1 "Enable one-shot trip-zone1 (TZ1)"; tzselOSHT2 "Enable one-shot trip-zone2 (TZ2)"; tzselOSHT3 "Enable one-shot trip-zone3 (TZ3)"; tzselOSHDCAEV1 "Enable one-shot digital compare A event 1 (DCAEVT1)"; tzselOSHDCBEV1 "Enable one-shot digital compare B event 1 (DCBEVT1)"; tzselCBC1 "Enable cyclic trip-zone1 (TZ1)"; tzselCBC2 "Enable cyclic trip-zone2 (TZ2)"; tzselCBC3 "Enable cyclic trip-zone3 (TZ3)"; tzselCBCDCAEV2 "Enable cyclic digital compare A event 2 (DCAEVT2)"; tzselCBCDCBEV2 "Enable cyclic digital compare B event 2 (DCBEVT2)"; tzselOSHT4 "Enable one-shot trip-zone4 (TZ4)"; tzselOSHT5 "Enable one-shot trip-zone5 (TZ5)"; tzselOSHT6 "Enable one-shot trip-zone6 (TZ6)"; tzselCBC4 "Enable cyclic trip-zone4 (TZ4)"; tzselCBC5 "Enable cyclic trip-zone5 (TZ5)"; tzselCBC6 "Enable cyclic trip-zone6 (TZ6)"; enTzOstIntr "Enable trip-zone one-shot interrupt (OST)"; enTzCbcIntr "Enable trip-zone cycle-by-cycle interrupt (CBC)"; enTzDCAEVT1Intr "Digital comparator output A event 1 interrupt enable (DCAEVT1)"; enTzDCAEVT2Intr "Digital comparator output A event 2 interrupt enable (DCAEVT2)"; enTzDCBEVT1Intr "Digital comparator output B event 1 interrupt enable (DCBEVT1)"; enTzDCBEVT2Intr "Digital comparator output B event 2 interrupt enable (DCBEVT2)"; ePWMxAforced "ePWM2A forced (TZ) to:"; ePWMxBforced "ePWM2B forced (TZ) to:"; DCAEVT1forced "ePWM2A forced (DCAEVT1) to:"; DCBEVT1forced "ePWM2B forced (DCBEVT1) to:"; DCAEVT2forced "ePWM2A forced (DCAEVT2) to:"; DCBEVT2forced "ePWM2B forced (DCBEVT2) to:"; dcah "Source for digital compare A high signal (DCAH):"; dcal "Source for digital compare A low signal (DCAL):"; dcbh "Source for digital compare B high signal (DCBH):"; dcbl "Source for digital compare B low signal (DCBL):"; dcah_type2 "Source for digital compare A high signal (DCAH):"; dcal_type2 "Source for digital compare A low signal (DCAL):"; dcbh_type2 "Source for digital compare B high signal (DCBH):"; dcbl_type2 "Source for digital compare B low signal (DCBL):"; gendcaevt1 "Digital compare output A event 1 selection (DCAEVT1):"; gendcaevt2 "Digital compare output A event 2 selection (DCAEVT2):"; gendcbevt1 "Digital compare output B event 1 selection (DCBEVT1):"; gendcbevt2 "Digital compare cutput B event 2 selection (DCBEVT2):"; dcaevt1src "DCAEVT1 source select:"; dcaevt2src "DCAEVT2 source select:"; dcbevt1src "DCBEVT1 source select:"; dcbevt2src "DCBEVT2 source select:"; pulsesel "Pulse select:"; blankinv "Blanking window inverted"; blankoffset "Blanking window offset"; blankwidth "Blanking window width"; evsrcsel "Filter source select:"; encape "Enable counter capture"
  wires:
  Constant6/1 -> Rate Transition5/1
  Rate Transition5/1 -> Eanble Output/1
  Rate Transition7/1 -> ePWM1_IGBT/3
  Duty Cycles/1(MOSFET_Duty_cycle) -> [MOSFET_Duty_Cycle]
  Duty Cycles/2(IGBT_Duty_Cycle) -> [IGBT_Duty_Cycle]
  [IGBT_Duty_Cycle] -> ePWM1_IGBT/2
  Rate Transition8/1 -> GreenLED/1
  Rate Transition9/1 -> BlueLED/1
  Rate Transition10/1 -> RedLED/1
  ADC_MOSFET_ON/1 -> Logic circuit/1(MOSFET_Enable)  "MOSFET_Enable"
  VoltMeas/1 -> Logic circuit/2(Volt_Protection)  "Volt_Protection"
  ADC_IGBT_ON/1 -> Logic circuit/3(IGBT_Enable)  "IGBT_Enable"
  Logic circuit/1(MOSFET_Enable1) -> Rate Transition3/1
  Logic circuit/3(IGBT_Enable1) -> Rate Transition7/1
  Logic circuit/2(LED) -> Demux/1
  Demux/1 -> Rate Transition10/1
  Demux/2 -> Rate Transition8/1
  Demux/3 -> Rate Transition9/1
  Rate Transition3/1 -> ePWM2_MOSFET/3
  [MOSFET_Duty_Cycle] -> ePWM2_MOSFET/2
  [IGBT_Timer] -> ePWM1_IGBT/1
  Timer/1(MOSFET) -> [MOSFET_Timer]
  [MOSFET_Timer] -> ePWM2_MOSFET/1
  Timer/2(IGBT) -> [IGBT_Timer]
  Dashboard receiver block/1(MOSFET_Vout) -> [MOSFET_Vout]
  Dashboard receiver block/2(MOSFET_fsw) -> [MOSFET_fsw]
  Dashboard receiver block/3(IGBT_Vout) -> [IGBT_Vout]
  Dashboard receiver block/4(IGBT_Fsw) -> [IGBT_fsw]
  [MOSFET_fsw] -> Timer/1(MOSFET_fsw)
  [IGBT_fsw] -> Timer/2(IGBT_fsw)
  [MOSFET_Vout] -> Duty Cycles/1(MOSFET_out)
  [MOSFET_fsw] -> Duty Cycles/2(MOSFET_fsw)
  [IGBT_Vout] -> Duty Cycles/3(IGBT_Vout)
  [IGBT_fsw] -> Duty Cycles/4(IGBT_fsw)
  Dashboard receiver block/5(Switch) -> Logic circuit/4(Switch)

== system Openloop_voltage_control/Dashboard receiver block ==
  Demux : Demux  Outputs=5
  Gain : Gain  Gain=1000
  Gain1 : Gain  Gain=1000
  SCI Receive : c280xlib/SCI Receive  sciModule=A  dataHead='S'  dataTail='E'  dataType=uint16  dataDim=5  initValue=0  errOption=Output the last received value  errValue=0  sampleTime=-1  outputStatus=off  postInterrupt=off  numFifo=1
  MOSFET_Vout : Outport
  MOSFET_fsw : Outport  Port=2
  IGBT_Vout : Outport  Port=3
  IGBT_Fsw : Outport  Port=4
  Switch : Outport  Port=5
  wires:
  SCI Receive/1 -> Demux/1
  Gain/1 -> MOSFET_fsw/1
  Gain1/1 -> IGBT_Fsw/1
  Demux/5 -> Gain1/1
  Demux/4 -> IGBT_Vout/1
  Demux/3 -> Gain/1
  Demux/2 -> MOSFET_Vout/1
  Demux/1 -> Switch/1

== system Openloop_voltage_control/Duty Cycles ==
  MOSFET_out : Inport
  MOSFET_fsw : Inport  Port=2
  IGBT_Vout : Inport  Port=3
  IGBT_fsw : Inport  Port=4
  Data Type Conversion : DataTypeConversion  OutDataTypeStr=uint16
  Data Type Conversion2 : DataTypeConversion  OutDataTypeStr=uint16
  Rate Transition : RateTransition
  Rate Transition6 : RateTransition
  Using parameter.m : Subsystem
  using dashboard.slx : Subsystem
  MOSFET_Duty_cycle : Outport
  IGBT_Duty_Cycle : Outport  Port=2
  wires:
  Data Type Conversion/1 -> Rate Transition/1
  Rate Transition/1 -> MOSFET_Duty_cycle/1
  Data Type Conversion2/1 -> Rate Transition6/1
  Rate Transition6/1 -> IGBT_Duty_Cycle/1
  MOSFET_out/1 -> using dashboard.slx/1(MOSFET_Vout)
  MOSFET_fsw/1 -> using dashboard.slx/2(MOSFET_fsw)
  IGBT_Vout/1 -> using dashboard.slx/3(IGBT_Vout)
  IGBT_fsw/1 -> using dashboard.slx/4(IGBT_fsw)
  using dashboard.slx/1(MOSFET) -> Data Type Conversion/1
  using dashboard.slx/2(IGBT) -> Data Type Conversion2/1

== system Openloop_voltage_control/Logic circuit ==
  MOSFET_Enable : Inport
  Volt_Protection : Inport  Port=2
  IGBT_Enable : Inport  Port=3
  Switch : Inport  Port=4
  Constant13 : Constant  Value=3350  OutDataTypeStr=uint16  SampleTime=-1
  Constant14 : Constant  Value=2500  OutDataTypeStr=uint16  SampleTime=-1
  Constant15 : Constant  OutDataTypeStr=boolean  SampleTime=-1
  Constant16 : Constant  OutDataTypeStr=boolean  SampleTime=-1
  Constant3 : Constant  Value=500  OutDataTypeStr=uint16  SampleTime=-1
  Constant8 : Constant  Value=500  OutDataTypeStr=uint16  SampleTime=-1
  Constant9 : Constant  Value=0  OutDataTypeStr=boolean  SampleTime=-1
  Data Type Conversion1 : DataTypeConversion  OutDataTypeStr=uint16
  Data Type Conversion4 : DataTypeConversion  OutDataTypeStr=uint16
  Logical Operator{,1,3,5..6} (5 alike) : Logic  Operator=OR  IconShape=distinctive  AllPortsSameDT=off  OutDataTypeStr=boolean
  Logical Operator2 : Logic  Operator=NOR  IconShape=distinctive  AllPortsSameDT=off  OutDataTypeStr=boolean
  Logical Operator4 : Logic  Operator=NOR  IconShape=distinctive  AllPortsSameDT=off  OutDataTypeStr=boolean
  Logical Operator7 : Logic  IconShape=distinctive  AllPortsSameDT=off  OutDataTypeStr=boolean
  Logical Operator8 : Logic  Operator=NAND  IconShape=distinctive  AllPortsSameDT=off  OutDataTypeStr=boolean
  MATLAB Function : MATLAB Function  TreatAsAtomicUnit=on
  Mux : Mux  Inputs=3
  NOT1 : Logic  Operator=NOT  IconShape=distinctive  AllPortsSameDT=off  OutDataTypeStr=boolean
  NOT2 : Logic  Operator=NOT  IconShape=distinctive  AllPortsSameDT=off  OutDataTypeStr=boolean
  NOT3 : Logic  Operator=NOT  IconShape=distinctive  AllPortsSameDT=off  OutDataTypeStr=boolean
  Relational Operator1 : RelationalOperator  Operator=<=  OutDataTypeStr=boolean  RndMeth=Simplest
  Relational Operator3 : RelationalOperator  Operator=<=  OutDataTypeStr=boolean  RndMeth=Simplest
  Relational Operator4 : RelationalOperator  OutDataTypeStr=boolean  RndMeth=Simplest
  Relational Operator5 : RelationalOperator  Operator=<=  OutDataTypeStr=boolean  RndMeth=Simplest
  Sample and Hold1 : dspsigops/Sample and Hold  trig=Rising edge  initCond=0  latchinput=off
  Sample and Hold2 : dspsigops/Sample and Hold  trig=Rising edge  initCond=0  latchinput=off
  Terminator : Terminator
  Terminator1 : Terminator
  MOSFET_Enable1 : Outport
  LED : Outport  Port=2
  IGBT_Enable1 : Outport  Port=3
  wires:
  Relational Operator1/1 -> Logical Operator7/1, Logical Operator4/1, Logical Operator/1
  Volt_Protection/1 -> Relational Operator4/2, Relational Operator5/1
  Logical Operator3/1 -> Data Type Conversion4/1, Logical Operator8/2
  Constant14/1 -> Relational Operator4/1
  Constant9/1 -> Logical Operator1/1, Logical Operator/2
  Logical Operator2/1 -> Sample and Hold2/Trigger
  Sample and Hold1/1 -> Logical Operator6/1, Logical Operator5/2
  Logical Operator5/1 -> Logical Operator8/1, Data Type Conversion1/1
  Constant15/1 -> Sample and Hold1/1
  Constant8/1 -> Relational Operator3/1
  Logical Operator8/1 -> NOT3/1
  Relational Operator3/1 -> Logical Operator7/2, Logical Operator2/2, Logical Operator1/2
  Data Type Conversion4/1 -> IGBT_Enable1/1  "IGBT_Enable"
  Logical Operator1/1 -> Logical Operator3/2
  Relational Operator4/1 -> Logical Operator4/2
  Logical Operator/1 -> Logical Operator5/1
  Relational Operator5/1 -> Logical Operator2/1
  Logical Operator4/1 -> Sample and Hold1/Trigger
  Sample and Hold2/1 -> Logical Operator3/1, Logical Operator6/2
  Constant3/1 -> Relational Operator1/1
  Constant16/1 -> Sample and Hold2/1
  Logical Operator7/1 -> NOT2/1
  Logical Operator6/1 -> NOT1/1
  Data Type Conversion1/1 -> MOSFET_Enable1/1  "MOSFET_Enable"
  NOT1/1 -> Mux/1  "RedLED"
  NOT2/1 -> Mux/2  "GreenLED"
  NOT3/1 -> Mux/3  "BLUELED"
  Mux/1 -> LED/1  "LED"
  Constant13/1 -> Relational Operator5/2
  Switch/1 -> MATLAB Function/1(u)
  MOSFET_Enable/1 -> Terminator/1
  IGBT_Enable/1 -> Terminator1/1
  MATLAB Function/1(y1) -> Relational Operator1/2
  MATLAB Function/2(y2) -> Relational Operator3/2

== system Openloop_voltage_control/Timer ==
  MOSFET_fsw : Inport
  IGBT_fsw : Inport  Port=2
  Using dashboard.slx : Subsystem
  Using parameter.m : Subsystem
  MOSFET : Outport
  IGBT : Outport  Port=2
  wires:
  MOSFET_fsw/1 -> Using dashboard.slx/1(MOSFET_fw)
  IGBT_fsw/1 -> Using dashboard.slx/2(IGBT_fsw)
  Using dashboard.slx/1(MOSFET) -> MOSFET/1
  Using dashboard.slx/2(IGBT) -> IGBT/1

== system Openloop_voltage_control/Duty Cycles/Using parameter.m ==
  Constant1 : Constant  Value=D_MOSFET_CCM
  Constant2 : Constant  Value=D_IGBT_CCM
  Gain : Gain  Gain=Timer_period_MOSFET
  Gain1 : Gain  Gain=Timer_period_IGBT
  MOSFET : Outport
  IGBT : Outport  Port=2
  wires:
  Constant1/1 -> Gain/1
  Gain/1 -> MOSFET/1
  Constant2/1 -> Gain1/1
  Gain1/1 -> IGBT/1

== system Openloop_voltage_control/Duty Cycles/using dashboard.slx ==
  note: 60MHz clock oscillator frequency. Look at hardware configuration-> Clocking
  MOSFET_Vout : Inport
  MOSFET_fsw : Inport  Port=2
  IGBT_Vout : Inport  Port=3
  IGBT_fsw : Inport  Port=4
  Add : Sum
  Add1 : Sum
  CLK frequency : Constant  Value=60e6
  Divide : Product  Inputs=/*
  Divide1 : Product  Inputs=*/
  Divide2 : Product  Inputs=*/
  Divide3 : Product  Inputs=*/
  Plus : Sum  Inputs=++-
  Plus1 : Sum  Inputs=++-
  Product : Product
  Product1 : Product
  V_f{,1..3} (4 alike) : Constant  Value=1.5
  V_in : Constant  Value=45
  V_in1 : Constant  Value=45
  MOSFET : Outport
  IGBT : Outport  Port=2
  wires:
  Product/1 -> MOSFET/1
  CLK frequency/1 -> Divide/2, Divide1/1
  Add/1 -> Divide2/2
  V_in/1 -> Plus/3
  V_f/1 -> Plus/2
  Plus/1 -> Divide2/1
  Divide/1 -> Product/2
  Divide2/1 -> Product/1
  V_f2/1 -> Plus1/2
  Plus1/1 -> Divide3/1
  Add1/1 -> Divide3/2
  Divide3/1 -> Product1/2
  V_in1/1 -> Plus1/3
  Product1/1 -> IGBT/1
  Divide1/1 -> Product1/1
  V_f1/1 -> Add/1
  V_f3/1 -> Add1/1
  MOSFET_fsw/1 -> Divide/1
  MOSFET_Vout/1 -> Add/2, Plus/1
  IGBT_Vout/1 -> Add1/2, Plus1/1
  IGBT_fsw/1 -> Divide1/2

== system Openloop_voltage_control/Timer/Using dashboard.slx ==
  MOSFET_fw : Inport
  IGBT_fsw : Inport  Port=2
  CLK frequency : Constant  Value=60e6
  CLK frequency1 : Constant  Value=60e6
  Divide : Product  Inputs=/*
  Divide1 : Product  Inputs=/*
  MOSFET : Outport
  IGBT : Outport  Port=2
  wires:
  Divide/1 -> MOSFET/1
  Divide1/1 -> IGBT/1
  MOSFET_fw/1 -> Divide/1
  CLK frequency/1 -> Divide/2
  CLK frequency1/1 -> Divide1/2
  IGBT_fsw/1 -> Divide1/1

== system Openloop_voltage_control/Timer/Using parameter.m ==
  Constant : Constant  Value=Timer_period_MOSFET
  Constant1 : Constant  Value=Timer_period_IGBT
  MOSFET : Outport
  IGBT : Outport  Port=2
  wires:
  Constant/1 -> MOSFET/1
  Constant1/1 -> IGBT/1

== matlab function Openloop_voltage_control/Logic circuit/MATLAB Function ==
function [y1,y2]= fcn(u)

if u==0;
    y1=1000;
    y2=1000;
elseif u == 1;
    y1=1000;
    y2=0;
elseif u==2; 
    y1=0;
    y2=1000;
else   
    y1=1000;
    y2=1000;
end
